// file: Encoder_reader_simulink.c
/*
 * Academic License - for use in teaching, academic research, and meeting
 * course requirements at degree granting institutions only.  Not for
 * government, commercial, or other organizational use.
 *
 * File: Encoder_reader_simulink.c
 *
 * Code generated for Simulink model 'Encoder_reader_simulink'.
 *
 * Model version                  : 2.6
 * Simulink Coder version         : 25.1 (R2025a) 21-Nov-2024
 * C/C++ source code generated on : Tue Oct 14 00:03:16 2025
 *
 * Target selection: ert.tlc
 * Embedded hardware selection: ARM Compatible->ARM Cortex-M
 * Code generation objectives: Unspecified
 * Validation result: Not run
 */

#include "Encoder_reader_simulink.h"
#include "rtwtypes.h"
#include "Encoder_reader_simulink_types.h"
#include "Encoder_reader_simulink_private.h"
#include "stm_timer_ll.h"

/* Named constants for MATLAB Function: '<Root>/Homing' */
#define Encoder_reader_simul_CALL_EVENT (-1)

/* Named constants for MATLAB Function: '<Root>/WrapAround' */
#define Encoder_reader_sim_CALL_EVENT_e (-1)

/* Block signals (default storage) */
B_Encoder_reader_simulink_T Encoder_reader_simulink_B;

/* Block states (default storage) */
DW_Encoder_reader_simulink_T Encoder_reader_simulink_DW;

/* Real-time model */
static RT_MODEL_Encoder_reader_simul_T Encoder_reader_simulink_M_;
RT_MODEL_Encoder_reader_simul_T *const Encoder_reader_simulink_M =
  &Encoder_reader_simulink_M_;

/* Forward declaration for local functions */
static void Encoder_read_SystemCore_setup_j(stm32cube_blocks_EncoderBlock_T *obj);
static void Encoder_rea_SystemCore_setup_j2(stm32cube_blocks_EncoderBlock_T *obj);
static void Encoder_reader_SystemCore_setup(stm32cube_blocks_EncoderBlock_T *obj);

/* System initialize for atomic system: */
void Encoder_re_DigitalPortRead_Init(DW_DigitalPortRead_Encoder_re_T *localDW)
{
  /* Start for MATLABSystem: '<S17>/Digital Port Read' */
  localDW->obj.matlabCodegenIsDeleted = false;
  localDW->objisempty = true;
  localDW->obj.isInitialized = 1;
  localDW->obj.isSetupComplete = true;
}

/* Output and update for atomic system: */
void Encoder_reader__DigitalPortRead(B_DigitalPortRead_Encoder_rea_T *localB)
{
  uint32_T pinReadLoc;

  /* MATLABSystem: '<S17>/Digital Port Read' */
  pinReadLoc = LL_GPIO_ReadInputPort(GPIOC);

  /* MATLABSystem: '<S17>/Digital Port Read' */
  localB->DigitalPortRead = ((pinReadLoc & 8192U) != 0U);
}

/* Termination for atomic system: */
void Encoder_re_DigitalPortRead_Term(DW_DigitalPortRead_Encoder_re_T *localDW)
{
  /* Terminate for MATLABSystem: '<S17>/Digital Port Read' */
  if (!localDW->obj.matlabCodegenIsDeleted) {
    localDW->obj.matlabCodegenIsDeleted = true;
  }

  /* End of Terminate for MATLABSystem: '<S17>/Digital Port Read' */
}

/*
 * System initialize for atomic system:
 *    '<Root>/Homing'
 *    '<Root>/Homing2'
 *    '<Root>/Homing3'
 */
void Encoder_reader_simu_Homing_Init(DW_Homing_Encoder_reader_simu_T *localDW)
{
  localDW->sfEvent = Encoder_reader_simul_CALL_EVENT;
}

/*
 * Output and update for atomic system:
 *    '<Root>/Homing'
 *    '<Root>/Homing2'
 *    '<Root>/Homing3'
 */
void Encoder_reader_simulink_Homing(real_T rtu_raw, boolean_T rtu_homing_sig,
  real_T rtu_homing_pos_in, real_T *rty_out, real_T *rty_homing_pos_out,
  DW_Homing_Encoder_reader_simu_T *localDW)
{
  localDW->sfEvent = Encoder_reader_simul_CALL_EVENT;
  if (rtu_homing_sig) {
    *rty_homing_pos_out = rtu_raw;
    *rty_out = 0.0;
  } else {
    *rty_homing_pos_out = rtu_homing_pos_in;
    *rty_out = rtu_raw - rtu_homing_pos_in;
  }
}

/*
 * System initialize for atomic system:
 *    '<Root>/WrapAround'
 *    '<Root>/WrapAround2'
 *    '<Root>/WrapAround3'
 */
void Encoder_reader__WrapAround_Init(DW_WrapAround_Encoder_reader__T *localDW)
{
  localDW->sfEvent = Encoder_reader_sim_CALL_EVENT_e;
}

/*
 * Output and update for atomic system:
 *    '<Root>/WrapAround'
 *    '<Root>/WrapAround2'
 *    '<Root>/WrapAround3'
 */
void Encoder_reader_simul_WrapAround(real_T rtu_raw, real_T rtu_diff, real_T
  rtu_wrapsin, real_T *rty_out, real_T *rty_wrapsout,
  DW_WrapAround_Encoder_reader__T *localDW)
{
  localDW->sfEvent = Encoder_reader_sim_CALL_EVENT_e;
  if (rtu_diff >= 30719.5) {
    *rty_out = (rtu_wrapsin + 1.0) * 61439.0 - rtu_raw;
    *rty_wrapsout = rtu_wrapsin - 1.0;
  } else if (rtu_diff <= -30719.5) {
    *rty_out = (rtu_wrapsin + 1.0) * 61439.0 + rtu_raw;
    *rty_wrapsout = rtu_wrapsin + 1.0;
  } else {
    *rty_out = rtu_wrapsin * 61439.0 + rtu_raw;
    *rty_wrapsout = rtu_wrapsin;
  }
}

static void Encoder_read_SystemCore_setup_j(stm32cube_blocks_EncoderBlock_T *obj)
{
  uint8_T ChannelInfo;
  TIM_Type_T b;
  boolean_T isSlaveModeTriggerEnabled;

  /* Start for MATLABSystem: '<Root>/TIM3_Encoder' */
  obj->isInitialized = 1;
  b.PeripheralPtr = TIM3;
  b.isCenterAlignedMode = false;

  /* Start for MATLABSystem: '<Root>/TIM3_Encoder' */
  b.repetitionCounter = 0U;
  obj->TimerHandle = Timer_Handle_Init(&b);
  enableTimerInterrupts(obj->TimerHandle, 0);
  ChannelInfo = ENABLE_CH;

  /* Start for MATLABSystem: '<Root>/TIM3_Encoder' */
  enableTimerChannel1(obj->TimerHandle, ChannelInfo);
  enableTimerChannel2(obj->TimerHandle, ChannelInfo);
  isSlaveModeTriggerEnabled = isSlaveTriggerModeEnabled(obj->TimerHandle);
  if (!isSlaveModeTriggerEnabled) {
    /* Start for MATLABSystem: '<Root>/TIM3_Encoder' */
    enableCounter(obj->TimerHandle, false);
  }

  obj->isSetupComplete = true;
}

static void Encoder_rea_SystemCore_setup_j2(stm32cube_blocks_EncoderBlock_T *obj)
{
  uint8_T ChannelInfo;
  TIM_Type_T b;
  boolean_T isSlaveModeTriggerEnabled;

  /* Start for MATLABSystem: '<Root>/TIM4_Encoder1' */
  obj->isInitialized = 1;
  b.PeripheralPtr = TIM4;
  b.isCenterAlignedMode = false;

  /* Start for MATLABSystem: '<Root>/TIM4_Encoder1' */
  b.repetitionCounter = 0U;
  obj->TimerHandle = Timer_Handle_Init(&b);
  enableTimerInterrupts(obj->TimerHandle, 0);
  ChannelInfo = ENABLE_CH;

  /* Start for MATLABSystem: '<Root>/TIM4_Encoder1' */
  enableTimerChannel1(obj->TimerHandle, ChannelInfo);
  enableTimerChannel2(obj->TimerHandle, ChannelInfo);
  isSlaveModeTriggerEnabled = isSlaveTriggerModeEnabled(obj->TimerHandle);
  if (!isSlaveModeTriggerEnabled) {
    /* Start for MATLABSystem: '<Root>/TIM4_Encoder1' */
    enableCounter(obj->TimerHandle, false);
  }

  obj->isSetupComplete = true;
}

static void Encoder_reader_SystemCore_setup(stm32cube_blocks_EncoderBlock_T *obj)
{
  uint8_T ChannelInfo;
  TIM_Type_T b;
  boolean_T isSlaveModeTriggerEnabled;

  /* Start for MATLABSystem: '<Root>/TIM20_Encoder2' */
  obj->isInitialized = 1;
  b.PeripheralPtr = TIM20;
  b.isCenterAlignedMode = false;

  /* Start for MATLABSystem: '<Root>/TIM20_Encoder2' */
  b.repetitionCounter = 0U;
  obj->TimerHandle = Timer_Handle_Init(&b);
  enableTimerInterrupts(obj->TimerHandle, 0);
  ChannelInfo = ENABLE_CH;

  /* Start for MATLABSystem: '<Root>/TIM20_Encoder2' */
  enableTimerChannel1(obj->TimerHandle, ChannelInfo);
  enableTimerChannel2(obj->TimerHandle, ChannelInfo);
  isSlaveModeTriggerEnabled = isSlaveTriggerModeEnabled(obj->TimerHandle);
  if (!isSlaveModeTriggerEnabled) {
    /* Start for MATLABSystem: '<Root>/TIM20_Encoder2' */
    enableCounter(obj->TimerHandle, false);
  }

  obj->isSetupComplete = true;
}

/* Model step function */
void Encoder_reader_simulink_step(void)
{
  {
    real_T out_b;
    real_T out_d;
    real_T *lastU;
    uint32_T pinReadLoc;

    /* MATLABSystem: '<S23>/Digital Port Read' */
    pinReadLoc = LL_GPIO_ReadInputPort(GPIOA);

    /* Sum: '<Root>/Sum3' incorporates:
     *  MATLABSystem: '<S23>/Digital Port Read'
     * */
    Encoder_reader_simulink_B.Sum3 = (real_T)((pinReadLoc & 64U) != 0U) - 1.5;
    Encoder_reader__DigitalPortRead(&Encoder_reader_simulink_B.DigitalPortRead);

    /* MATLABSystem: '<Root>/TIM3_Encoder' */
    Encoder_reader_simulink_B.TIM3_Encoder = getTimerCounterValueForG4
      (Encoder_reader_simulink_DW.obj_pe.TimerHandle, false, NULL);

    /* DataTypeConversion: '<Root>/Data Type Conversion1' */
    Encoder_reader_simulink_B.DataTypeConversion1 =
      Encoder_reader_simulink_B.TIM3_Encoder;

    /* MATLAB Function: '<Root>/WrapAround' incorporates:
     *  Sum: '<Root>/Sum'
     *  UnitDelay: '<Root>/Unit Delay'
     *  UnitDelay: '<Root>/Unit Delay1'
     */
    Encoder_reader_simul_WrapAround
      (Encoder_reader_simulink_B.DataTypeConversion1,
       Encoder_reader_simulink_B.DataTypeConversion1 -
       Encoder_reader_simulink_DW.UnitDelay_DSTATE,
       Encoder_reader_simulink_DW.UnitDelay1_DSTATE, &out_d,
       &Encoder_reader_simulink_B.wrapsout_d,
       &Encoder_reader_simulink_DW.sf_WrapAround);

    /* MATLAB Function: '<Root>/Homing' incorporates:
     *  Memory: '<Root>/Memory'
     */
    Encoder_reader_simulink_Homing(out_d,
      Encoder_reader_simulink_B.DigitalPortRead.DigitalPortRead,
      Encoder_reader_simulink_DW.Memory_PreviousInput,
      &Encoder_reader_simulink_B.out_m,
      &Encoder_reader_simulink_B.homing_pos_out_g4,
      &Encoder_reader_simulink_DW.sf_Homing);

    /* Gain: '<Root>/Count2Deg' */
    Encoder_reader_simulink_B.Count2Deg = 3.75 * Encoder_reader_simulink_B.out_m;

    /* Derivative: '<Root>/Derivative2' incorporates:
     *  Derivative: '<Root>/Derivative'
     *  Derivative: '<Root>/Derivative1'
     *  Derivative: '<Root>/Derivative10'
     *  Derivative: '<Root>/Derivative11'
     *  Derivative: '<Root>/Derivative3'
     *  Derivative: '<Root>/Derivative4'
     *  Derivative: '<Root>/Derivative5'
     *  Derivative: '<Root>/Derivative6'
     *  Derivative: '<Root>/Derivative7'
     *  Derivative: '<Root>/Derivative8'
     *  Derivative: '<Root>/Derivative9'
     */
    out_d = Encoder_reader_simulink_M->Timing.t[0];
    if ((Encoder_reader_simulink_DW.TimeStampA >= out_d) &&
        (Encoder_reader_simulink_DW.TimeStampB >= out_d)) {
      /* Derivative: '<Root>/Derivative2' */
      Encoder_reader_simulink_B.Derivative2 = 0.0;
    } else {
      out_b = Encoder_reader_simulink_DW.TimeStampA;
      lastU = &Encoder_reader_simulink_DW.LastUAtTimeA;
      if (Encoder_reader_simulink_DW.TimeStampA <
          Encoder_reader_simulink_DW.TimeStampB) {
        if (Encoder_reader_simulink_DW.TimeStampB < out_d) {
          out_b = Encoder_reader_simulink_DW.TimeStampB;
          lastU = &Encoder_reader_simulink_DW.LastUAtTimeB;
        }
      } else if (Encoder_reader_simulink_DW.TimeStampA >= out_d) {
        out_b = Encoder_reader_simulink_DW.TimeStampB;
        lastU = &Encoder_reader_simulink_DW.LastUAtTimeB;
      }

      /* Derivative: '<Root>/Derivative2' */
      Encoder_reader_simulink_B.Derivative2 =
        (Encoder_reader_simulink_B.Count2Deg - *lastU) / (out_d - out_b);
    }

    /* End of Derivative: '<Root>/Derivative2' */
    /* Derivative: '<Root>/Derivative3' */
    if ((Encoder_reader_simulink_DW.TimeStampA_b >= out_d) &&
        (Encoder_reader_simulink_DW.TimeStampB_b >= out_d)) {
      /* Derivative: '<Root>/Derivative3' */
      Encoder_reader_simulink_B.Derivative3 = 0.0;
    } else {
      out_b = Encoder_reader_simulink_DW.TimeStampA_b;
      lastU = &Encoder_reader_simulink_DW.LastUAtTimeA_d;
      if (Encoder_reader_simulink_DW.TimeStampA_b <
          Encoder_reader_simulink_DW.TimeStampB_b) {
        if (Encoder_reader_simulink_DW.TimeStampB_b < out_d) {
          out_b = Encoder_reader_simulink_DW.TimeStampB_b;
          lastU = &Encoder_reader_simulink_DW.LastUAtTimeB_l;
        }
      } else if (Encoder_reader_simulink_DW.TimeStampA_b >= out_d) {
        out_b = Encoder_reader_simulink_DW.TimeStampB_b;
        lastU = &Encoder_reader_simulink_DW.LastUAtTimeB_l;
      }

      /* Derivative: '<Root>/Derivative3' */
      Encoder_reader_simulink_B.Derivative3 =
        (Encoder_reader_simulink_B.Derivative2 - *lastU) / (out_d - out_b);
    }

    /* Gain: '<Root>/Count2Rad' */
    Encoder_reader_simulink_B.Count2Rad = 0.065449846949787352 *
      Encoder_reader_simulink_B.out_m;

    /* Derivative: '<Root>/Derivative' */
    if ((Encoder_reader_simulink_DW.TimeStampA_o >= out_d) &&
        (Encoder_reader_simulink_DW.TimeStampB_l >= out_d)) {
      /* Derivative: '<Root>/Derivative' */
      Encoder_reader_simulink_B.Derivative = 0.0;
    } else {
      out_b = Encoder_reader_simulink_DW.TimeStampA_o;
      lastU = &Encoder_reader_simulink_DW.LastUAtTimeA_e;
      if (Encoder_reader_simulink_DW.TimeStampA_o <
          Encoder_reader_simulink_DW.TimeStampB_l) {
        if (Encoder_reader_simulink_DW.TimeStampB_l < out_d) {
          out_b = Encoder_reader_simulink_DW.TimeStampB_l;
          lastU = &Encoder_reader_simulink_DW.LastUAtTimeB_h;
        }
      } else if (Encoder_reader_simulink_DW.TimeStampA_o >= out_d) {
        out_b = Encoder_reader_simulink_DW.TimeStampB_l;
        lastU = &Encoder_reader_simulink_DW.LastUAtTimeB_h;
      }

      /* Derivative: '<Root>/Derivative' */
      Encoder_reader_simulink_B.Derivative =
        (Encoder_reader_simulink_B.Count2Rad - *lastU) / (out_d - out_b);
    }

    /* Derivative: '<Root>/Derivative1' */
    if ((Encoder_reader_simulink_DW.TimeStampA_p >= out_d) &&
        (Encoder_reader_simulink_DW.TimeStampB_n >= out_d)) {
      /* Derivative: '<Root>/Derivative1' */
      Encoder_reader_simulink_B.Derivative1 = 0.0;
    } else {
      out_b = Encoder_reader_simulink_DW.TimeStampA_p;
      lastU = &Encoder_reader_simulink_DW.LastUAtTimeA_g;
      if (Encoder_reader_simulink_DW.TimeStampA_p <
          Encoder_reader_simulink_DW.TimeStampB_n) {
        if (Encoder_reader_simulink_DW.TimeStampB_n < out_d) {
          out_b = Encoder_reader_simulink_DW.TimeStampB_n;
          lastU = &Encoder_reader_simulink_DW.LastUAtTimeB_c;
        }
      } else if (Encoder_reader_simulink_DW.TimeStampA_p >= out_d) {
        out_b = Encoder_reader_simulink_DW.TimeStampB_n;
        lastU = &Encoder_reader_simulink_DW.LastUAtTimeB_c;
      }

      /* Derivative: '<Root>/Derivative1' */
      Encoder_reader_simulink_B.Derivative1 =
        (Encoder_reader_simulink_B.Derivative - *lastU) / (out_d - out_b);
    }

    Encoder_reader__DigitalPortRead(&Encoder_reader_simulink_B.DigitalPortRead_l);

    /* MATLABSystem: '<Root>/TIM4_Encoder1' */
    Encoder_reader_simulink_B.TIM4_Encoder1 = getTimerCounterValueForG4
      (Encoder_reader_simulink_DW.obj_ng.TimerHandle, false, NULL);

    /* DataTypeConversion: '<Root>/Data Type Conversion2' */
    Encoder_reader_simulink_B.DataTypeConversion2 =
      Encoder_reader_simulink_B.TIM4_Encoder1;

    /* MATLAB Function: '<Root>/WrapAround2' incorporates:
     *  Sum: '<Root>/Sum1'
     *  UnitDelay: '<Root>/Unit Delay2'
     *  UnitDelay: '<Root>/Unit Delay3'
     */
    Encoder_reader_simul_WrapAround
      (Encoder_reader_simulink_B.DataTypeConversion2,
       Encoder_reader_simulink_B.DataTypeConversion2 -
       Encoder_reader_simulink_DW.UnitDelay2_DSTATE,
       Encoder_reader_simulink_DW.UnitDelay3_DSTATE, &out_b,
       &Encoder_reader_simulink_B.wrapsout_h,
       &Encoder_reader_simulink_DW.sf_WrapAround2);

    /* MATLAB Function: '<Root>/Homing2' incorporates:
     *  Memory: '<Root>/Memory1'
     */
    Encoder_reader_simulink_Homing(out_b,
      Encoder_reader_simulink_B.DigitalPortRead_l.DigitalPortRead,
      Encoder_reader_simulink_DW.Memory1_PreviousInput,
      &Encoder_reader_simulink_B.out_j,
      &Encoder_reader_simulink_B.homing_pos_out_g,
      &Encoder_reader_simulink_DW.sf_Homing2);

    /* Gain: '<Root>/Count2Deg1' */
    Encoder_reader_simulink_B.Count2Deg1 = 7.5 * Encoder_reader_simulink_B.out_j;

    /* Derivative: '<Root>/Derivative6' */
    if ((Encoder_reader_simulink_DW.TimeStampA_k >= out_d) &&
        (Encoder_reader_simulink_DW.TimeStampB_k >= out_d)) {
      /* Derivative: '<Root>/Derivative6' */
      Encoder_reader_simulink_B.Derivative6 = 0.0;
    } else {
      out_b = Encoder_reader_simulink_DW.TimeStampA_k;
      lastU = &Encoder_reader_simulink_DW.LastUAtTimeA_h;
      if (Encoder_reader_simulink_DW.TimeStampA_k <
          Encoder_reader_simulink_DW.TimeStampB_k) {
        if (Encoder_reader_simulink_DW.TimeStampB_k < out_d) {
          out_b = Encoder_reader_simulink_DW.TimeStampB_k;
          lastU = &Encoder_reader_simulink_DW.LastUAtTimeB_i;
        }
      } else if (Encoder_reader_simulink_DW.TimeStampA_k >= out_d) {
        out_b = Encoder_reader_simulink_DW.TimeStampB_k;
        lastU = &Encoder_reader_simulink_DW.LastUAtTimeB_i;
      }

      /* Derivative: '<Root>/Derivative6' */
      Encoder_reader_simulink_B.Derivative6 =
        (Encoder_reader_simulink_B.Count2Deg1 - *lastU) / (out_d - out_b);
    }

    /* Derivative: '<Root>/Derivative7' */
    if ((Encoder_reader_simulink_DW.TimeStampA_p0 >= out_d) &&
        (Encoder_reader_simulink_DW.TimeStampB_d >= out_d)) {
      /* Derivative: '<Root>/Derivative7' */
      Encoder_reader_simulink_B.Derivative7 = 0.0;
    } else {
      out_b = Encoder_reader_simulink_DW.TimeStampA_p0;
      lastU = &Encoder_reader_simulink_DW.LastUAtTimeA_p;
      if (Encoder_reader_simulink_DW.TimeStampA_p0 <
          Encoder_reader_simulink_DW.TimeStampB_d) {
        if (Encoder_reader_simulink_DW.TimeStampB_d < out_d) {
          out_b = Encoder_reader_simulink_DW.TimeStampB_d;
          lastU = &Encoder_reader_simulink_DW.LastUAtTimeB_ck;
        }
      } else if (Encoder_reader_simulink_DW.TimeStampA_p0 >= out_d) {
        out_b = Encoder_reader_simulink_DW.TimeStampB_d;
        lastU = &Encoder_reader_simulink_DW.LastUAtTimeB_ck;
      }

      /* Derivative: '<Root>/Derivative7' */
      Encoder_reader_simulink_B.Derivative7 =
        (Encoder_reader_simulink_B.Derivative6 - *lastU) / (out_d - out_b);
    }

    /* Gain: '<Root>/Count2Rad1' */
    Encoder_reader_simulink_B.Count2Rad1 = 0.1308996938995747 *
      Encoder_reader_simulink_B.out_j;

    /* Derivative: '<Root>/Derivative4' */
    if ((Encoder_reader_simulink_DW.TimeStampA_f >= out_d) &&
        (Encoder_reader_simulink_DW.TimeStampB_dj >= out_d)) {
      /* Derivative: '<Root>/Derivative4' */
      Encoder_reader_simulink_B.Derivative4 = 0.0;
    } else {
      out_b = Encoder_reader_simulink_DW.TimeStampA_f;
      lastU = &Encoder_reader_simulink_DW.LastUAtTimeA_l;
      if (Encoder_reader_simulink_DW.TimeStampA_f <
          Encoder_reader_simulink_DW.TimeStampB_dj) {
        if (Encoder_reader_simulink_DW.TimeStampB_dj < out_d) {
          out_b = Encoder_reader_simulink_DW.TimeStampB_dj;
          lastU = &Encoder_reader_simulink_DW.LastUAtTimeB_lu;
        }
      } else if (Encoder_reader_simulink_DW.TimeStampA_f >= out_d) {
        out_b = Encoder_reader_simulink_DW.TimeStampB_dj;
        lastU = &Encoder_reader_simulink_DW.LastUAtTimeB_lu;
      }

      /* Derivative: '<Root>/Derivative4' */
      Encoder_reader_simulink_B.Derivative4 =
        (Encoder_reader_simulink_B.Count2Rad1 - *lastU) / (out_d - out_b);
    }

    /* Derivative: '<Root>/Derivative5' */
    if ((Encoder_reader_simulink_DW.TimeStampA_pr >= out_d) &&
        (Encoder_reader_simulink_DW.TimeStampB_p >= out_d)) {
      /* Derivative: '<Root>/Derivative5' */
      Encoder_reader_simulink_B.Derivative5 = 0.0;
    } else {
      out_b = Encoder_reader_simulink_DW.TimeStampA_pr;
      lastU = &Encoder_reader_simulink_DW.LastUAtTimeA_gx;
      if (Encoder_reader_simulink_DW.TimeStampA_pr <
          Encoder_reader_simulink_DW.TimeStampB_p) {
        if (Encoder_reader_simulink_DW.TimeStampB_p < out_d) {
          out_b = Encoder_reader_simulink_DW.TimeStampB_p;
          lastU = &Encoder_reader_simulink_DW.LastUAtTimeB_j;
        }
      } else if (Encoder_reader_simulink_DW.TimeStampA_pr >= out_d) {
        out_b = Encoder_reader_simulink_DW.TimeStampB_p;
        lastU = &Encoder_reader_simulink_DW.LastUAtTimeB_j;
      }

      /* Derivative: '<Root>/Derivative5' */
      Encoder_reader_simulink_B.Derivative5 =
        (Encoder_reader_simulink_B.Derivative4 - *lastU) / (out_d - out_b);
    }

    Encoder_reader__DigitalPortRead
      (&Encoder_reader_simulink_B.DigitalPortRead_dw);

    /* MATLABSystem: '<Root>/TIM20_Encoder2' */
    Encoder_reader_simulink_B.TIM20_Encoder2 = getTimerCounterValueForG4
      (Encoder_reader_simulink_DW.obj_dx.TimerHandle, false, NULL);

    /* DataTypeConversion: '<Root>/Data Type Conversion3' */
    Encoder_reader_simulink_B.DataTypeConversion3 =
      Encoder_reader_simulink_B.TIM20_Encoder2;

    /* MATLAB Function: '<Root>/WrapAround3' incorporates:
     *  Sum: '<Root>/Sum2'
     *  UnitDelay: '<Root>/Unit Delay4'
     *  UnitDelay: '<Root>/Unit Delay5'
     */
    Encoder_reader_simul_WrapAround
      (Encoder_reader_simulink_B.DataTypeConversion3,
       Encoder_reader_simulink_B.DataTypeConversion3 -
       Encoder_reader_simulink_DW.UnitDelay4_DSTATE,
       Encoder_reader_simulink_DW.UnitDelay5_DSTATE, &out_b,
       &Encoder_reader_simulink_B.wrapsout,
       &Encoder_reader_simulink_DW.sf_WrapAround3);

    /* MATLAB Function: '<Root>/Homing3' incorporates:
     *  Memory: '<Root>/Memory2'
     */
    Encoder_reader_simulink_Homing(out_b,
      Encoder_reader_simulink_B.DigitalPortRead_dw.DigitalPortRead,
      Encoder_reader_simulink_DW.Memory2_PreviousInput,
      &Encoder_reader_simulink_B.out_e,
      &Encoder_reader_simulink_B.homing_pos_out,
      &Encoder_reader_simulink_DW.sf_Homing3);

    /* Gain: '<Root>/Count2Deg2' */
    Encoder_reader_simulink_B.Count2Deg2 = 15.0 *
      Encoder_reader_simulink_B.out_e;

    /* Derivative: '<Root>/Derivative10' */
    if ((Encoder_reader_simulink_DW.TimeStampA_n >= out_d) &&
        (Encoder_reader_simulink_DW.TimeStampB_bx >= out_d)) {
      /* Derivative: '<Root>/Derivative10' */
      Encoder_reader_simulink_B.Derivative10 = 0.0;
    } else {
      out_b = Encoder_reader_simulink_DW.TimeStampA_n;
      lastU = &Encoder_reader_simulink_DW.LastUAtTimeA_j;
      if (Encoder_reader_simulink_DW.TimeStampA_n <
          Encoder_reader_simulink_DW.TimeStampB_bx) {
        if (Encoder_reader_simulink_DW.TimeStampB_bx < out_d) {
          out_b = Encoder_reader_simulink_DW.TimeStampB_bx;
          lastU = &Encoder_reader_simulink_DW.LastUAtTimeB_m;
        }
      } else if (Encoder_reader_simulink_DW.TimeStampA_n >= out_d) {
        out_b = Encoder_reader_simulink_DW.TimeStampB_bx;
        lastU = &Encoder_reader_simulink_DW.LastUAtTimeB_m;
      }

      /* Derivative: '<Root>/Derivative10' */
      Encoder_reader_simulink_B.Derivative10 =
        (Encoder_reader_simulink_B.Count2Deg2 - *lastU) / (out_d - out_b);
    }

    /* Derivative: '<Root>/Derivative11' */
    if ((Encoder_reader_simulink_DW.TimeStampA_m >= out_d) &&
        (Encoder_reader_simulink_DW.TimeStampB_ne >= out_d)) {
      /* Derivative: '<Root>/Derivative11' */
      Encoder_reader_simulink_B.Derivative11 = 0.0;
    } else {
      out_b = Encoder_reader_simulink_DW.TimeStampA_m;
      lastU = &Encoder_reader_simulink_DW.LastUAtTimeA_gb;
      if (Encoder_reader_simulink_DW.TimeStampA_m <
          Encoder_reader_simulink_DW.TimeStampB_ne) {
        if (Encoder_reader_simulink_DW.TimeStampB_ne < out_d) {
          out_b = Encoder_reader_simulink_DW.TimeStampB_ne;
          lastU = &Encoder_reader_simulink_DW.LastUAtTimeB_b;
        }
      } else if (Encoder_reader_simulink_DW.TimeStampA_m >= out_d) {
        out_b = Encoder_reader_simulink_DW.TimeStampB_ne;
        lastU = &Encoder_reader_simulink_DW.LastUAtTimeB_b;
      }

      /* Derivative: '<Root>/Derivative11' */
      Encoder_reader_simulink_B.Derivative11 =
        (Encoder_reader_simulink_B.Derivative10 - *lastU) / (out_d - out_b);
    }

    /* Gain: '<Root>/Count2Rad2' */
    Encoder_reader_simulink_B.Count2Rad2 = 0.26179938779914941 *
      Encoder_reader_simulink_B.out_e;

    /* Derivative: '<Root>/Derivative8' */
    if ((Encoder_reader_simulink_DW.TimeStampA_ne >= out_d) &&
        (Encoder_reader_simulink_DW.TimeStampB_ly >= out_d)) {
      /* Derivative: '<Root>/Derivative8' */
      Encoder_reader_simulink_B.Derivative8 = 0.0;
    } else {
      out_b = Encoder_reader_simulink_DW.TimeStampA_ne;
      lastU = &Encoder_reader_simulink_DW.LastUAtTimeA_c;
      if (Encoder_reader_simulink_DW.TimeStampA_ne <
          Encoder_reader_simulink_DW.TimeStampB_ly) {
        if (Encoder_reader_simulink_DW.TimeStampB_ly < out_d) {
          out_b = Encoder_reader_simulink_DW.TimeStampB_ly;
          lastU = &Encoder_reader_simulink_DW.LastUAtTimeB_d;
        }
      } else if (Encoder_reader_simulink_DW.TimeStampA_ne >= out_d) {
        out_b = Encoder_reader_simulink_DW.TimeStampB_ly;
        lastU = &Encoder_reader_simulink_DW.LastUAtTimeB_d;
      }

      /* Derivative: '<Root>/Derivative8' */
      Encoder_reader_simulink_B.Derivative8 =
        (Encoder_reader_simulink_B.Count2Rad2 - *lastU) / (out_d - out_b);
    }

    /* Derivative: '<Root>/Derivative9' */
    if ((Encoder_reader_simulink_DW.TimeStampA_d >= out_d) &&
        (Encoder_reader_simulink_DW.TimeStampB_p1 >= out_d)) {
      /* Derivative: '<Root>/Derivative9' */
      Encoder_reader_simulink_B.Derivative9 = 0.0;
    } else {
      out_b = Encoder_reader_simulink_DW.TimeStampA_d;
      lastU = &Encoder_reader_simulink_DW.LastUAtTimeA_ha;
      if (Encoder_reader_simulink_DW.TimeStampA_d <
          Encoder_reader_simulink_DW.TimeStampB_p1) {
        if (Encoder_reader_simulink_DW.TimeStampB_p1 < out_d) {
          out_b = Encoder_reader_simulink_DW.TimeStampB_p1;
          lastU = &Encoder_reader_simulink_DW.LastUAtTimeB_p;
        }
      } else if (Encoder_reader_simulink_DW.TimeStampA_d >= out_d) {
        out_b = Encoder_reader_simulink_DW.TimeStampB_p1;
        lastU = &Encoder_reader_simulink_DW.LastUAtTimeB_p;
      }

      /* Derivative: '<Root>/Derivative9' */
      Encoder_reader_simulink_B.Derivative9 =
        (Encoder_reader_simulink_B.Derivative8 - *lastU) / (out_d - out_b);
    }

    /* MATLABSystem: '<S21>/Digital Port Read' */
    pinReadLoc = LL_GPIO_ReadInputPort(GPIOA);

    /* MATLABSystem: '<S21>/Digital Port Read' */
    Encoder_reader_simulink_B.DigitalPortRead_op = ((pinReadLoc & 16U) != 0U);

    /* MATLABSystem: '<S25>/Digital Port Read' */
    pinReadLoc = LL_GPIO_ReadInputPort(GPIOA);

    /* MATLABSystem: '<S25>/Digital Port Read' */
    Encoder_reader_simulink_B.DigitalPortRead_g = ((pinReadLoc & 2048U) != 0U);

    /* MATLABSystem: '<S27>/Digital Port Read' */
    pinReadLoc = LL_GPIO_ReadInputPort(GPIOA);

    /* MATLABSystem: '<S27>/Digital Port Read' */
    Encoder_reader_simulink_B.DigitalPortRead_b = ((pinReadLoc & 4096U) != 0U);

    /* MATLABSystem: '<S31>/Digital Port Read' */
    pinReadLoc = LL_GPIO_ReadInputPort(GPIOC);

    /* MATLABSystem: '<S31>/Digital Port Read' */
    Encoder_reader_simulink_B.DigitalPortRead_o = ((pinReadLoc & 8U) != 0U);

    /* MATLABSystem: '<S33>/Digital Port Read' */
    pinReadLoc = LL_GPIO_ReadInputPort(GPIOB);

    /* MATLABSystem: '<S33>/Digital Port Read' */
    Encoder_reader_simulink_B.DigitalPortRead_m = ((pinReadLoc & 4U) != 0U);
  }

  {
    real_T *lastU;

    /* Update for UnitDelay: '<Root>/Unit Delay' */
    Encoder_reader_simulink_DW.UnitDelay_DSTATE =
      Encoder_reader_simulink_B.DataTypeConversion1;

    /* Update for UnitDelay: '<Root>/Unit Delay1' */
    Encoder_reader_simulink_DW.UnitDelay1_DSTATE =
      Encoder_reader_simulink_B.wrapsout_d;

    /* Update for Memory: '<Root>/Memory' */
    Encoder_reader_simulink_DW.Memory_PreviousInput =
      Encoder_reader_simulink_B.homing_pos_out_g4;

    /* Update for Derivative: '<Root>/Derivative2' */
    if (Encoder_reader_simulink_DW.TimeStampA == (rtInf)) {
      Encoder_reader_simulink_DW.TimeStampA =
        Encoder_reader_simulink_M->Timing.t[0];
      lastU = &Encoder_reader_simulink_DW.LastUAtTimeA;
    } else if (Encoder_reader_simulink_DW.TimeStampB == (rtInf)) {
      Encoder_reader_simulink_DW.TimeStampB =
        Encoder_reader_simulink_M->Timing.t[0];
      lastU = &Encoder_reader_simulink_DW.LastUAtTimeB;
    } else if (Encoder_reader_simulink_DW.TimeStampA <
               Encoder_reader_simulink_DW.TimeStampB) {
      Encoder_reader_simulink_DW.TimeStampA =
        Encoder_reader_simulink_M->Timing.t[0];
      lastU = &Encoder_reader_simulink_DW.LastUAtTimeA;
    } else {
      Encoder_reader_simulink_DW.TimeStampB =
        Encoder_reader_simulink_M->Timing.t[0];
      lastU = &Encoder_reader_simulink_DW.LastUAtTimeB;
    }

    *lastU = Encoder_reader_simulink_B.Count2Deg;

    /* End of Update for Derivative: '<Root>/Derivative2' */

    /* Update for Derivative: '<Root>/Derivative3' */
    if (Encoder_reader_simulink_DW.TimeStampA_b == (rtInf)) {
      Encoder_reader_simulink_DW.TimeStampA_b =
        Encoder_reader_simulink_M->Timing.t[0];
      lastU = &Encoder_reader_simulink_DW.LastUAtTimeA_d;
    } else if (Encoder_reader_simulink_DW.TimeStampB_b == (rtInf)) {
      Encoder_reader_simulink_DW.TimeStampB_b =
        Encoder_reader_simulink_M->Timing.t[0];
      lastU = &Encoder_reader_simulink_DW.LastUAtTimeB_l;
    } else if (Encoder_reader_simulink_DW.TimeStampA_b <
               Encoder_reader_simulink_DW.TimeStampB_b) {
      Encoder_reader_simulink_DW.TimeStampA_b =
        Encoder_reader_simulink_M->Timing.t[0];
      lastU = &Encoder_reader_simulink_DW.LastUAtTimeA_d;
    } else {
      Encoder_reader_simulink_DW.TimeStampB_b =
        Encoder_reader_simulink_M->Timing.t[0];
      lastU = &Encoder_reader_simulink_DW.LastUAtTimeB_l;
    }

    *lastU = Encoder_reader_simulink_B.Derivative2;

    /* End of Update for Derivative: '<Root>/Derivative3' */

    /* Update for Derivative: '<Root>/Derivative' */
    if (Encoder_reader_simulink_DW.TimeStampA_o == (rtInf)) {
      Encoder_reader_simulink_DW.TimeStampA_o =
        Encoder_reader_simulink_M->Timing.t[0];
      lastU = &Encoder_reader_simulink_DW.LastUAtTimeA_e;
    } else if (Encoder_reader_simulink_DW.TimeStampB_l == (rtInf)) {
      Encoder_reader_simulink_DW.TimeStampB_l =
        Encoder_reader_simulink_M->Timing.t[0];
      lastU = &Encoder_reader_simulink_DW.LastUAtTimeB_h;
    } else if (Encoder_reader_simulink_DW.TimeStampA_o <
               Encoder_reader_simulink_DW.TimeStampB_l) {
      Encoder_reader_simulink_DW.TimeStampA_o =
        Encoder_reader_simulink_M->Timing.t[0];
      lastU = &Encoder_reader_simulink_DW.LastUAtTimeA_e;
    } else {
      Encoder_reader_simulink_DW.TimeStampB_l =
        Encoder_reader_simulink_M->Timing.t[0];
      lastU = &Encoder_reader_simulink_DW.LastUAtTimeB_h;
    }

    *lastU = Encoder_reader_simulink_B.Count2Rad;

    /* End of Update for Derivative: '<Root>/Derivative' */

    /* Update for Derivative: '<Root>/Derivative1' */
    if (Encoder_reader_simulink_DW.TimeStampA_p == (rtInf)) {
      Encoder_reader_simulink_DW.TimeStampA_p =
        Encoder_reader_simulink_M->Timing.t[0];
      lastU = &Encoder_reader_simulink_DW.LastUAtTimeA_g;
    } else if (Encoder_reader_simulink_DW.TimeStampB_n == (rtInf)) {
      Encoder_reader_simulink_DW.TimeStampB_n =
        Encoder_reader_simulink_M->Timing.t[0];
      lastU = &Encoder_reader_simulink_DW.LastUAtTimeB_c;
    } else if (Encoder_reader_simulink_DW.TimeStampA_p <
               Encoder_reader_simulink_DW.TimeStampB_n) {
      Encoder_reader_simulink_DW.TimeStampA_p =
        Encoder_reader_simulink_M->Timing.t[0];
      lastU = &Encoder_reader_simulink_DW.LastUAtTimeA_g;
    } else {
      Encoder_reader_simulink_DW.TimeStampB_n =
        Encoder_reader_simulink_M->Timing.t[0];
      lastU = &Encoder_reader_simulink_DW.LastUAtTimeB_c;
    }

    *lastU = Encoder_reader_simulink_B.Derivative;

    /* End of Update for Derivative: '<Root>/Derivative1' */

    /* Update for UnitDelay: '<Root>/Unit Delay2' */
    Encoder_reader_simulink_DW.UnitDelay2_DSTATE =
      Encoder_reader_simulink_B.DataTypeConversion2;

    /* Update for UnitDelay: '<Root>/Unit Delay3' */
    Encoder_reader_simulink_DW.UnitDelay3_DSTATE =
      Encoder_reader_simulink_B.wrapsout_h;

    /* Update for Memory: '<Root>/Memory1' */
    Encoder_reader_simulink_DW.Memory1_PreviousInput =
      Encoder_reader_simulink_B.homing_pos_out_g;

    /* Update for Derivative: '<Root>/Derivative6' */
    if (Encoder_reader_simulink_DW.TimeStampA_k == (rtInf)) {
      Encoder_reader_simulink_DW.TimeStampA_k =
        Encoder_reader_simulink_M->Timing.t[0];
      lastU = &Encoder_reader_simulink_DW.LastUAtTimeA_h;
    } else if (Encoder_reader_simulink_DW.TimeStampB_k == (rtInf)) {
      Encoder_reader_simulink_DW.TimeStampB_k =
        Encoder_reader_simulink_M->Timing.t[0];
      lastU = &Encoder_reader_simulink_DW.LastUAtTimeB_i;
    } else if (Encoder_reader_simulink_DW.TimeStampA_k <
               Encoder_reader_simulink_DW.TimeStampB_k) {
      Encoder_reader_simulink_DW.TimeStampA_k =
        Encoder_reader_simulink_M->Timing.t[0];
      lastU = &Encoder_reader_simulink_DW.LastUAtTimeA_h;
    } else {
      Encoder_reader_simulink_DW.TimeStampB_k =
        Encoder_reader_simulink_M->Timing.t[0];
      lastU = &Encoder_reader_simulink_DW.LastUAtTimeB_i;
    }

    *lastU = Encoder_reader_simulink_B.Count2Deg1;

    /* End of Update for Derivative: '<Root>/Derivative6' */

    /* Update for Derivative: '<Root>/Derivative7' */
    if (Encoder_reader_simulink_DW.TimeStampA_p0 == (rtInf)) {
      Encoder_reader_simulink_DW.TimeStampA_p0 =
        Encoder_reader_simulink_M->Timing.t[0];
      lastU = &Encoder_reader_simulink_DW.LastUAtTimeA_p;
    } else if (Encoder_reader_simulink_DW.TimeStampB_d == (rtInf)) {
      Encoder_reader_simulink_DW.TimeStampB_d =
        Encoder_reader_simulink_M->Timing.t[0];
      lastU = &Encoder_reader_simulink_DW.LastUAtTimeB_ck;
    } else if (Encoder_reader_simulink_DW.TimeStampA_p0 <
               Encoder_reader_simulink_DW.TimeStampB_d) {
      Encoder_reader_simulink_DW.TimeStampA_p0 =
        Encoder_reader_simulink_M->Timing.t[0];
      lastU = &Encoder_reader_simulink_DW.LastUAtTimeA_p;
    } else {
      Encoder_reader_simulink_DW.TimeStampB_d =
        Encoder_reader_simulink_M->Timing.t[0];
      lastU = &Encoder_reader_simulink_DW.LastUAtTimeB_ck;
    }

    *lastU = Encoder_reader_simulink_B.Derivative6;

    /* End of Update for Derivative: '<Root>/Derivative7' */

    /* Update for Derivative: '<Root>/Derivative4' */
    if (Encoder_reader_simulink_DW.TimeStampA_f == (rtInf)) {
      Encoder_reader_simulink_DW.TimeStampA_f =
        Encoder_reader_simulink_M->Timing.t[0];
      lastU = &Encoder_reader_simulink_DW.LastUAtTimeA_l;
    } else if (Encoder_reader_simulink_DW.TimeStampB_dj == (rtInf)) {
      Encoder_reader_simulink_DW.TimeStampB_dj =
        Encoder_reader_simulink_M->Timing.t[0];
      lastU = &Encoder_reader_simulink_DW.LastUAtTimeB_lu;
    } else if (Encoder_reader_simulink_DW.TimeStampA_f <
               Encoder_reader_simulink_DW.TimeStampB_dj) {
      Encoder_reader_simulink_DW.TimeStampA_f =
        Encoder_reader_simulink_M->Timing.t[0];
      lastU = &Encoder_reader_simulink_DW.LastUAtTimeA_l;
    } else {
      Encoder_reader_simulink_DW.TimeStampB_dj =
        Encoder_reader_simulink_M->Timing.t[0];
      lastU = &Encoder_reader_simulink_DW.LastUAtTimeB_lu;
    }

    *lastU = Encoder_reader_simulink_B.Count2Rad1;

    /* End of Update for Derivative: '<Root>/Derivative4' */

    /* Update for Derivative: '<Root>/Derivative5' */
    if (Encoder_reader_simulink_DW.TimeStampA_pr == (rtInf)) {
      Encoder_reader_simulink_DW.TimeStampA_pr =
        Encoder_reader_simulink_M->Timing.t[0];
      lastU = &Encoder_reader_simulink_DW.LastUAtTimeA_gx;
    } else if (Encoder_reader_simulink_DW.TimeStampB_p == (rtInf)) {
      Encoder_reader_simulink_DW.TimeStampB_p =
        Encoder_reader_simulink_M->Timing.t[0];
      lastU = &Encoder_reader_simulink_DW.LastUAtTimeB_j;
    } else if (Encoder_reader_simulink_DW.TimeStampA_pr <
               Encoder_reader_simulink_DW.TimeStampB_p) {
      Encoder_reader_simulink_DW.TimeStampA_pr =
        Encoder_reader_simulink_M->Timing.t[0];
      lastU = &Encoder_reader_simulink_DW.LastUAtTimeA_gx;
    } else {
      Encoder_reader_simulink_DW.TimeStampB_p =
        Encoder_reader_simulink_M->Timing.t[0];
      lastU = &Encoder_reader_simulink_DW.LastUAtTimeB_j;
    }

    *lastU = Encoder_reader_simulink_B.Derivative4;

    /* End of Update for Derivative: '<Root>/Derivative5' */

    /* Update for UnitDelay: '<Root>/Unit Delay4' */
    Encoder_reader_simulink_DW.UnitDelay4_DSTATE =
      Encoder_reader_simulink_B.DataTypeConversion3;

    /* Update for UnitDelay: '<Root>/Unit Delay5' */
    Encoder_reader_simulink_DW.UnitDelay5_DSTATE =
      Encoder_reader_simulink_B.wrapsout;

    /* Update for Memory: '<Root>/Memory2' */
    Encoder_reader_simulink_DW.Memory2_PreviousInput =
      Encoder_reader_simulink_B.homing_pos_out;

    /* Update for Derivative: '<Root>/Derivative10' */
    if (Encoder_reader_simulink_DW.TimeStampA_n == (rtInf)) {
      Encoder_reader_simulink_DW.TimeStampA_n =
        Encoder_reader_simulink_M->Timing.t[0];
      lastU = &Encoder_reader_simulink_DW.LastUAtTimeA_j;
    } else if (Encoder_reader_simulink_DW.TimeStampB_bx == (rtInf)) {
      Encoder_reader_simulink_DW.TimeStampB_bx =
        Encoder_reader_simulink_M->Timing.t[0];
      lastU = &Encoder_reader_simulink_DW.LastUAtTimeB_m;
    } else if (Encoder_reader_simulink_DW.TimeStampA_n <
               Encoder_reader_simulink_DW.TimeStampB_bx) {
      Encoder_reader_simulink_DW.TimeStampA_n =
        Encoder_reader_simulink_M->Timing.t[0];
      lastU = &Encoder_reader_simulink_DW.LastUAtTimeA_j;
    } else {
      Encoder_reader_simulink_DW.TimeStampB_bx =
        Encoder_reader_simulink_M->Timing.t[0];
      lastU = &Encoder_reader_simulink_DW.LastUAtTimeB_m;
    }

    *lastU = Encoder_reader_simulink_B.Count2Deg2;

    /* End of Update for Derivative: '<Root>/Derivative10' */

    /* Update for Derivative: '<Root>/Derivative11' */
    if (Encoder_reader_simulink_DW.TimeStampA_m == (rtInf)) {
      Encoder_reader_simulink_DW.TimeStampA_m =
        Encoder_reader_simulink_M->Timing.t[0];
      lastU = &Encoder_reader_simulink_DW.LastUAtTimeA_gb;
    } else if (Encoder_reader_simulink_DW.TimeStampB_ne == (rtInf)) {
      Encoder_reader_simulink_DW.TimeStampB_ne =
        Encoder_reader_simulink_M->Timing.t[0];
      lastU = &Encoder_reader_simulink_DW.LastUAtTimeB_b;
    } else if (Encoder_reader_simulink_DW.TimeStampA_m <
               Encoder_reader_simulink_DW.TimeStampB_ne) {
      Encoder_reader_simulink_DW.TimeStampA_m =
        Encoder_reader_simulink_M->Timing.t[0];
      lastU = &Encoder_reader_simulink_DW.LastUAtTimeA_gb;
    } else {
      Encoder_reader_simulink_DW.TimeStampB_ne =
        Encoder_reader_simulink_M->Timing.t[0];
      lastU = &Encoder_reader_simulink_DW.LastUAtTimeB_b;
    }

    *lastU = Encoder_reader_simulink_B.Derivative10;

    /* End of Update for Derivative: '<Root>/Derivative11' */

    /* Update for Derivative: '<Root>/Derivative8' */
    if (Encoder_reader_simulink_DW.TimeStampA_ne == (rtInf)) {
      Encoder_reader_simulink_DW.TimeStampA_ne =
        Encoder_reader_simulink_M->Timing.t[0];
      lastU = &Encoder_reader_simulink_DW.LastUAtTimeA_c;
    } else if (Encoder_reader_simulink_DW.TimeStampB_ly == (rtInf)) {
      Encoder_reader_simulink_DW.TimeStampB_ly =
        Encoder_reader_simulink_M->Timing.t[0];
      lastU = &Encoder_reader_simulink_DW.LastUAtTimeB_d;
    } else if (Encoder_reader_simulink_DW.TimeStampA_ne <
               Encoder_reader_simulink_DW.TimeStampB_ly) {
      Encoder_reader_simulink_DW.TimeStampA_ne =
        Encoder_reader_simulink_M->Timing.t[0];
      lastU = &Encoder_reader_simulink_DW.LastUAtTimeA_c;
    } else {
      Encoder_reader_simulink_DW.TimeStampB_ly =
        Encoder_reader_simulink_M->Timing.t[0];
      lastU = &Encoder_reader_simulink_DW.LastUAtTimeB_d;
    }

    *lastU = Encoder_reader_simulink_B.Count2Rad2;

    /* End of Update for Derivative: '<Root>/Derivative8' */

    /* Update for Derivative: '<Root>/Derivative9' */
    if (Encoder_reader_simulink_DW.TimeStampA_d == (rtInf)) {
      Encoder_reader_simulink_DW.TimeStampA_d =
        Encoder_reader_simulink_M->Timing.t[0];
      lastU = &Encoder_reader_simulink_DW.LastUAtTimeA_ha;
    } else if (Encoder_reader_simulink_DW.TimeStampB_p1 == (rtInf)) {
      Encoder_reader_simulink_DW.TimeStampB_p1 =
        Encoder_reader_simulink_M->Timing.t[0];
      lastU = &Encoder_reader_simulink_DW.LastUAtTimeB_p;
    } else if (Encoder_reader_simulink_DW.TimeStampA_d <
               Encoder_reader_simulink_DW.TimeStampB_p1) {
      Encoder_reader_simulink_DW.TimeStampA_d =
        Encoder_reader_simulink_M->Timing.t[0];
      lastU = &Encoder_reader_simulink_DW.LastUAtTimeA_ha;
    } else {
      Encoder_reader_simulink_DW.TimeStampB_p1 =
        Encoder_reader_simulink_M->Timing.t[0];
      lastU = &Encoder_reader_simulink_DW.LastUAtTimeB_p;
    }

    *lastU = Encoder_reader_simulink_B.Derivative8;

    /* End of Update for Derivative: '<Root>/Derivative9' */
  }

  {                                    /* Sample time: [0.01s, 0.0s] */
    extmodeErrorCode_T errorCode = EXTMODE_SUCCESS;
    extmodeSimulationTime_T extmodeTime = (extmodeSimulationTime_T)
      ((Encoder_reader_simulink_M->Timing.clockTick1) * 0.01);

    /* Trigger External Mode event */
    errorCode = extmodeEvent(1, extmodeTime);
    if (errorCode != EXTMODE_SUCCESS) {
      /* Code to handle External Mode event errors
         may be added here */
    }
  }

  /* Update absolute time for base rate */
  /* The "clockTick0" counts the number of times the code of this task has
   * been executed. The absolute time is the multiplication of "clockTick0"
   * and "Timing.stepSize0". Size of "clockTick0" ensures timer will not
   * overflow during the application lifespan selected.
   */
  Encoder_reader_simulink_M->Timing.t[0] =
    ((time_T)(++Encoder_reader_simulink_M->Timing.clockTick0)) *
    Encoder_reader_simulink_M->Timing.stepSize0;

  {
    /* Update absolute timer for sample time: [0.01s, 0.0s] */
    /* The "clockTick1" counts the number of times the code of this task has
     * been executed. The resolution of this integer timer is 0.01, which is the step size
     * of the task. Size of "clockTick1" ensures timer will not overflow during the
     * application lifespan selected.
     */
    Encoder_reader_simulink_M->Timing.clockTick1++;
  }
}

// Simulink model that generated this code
simulink model "Encoder_reader_simulink"  (R2025a)
settings: Solver=FixedStepAuto  StartTime=0.0  StopTime=inf  FixedStep=0.01  RelTol=1e-3  EnableMultiTasking=on
libraries: stm32f4xxblockslib x18, stm32g4xxblockslib x6

== system Encoder_reader_simulink ==
  note: Rotary Encoder
  note: AMT103 Encoder
  Constant : Constant  Value=-1.5
  Constant1 : Constant  Commented=on  Value=-1.5
  Count2Deg : Gain  Gain=360/96
  Count2Deg1 : Gain  Gain=360/48
  Count2Deg2 : Gain  Gain=360/24
  Count2Deg3 : Gain  Commented=on  Gain=360/8192
  Count2Deg4 : Gain  Commented=on  Gain=360/4096
  Count2Deg5 : Gain  Commented=on  Gain=360/2048
  Count2Rad : Gain  Gain=2*pi/96
  Count2Rad1 : Gain  Gain=2*pi/48
  Count2Rad2 : Gain  Gain=2*pi/24
  Count2Rad3 : Gain  Commented=on  Gain=2*pi/8192
  Count2Rad4 : Gain  Commented=on  Gain=2*pi/4096
  Count2Rad5 : Gain  Commented=on  Gain=2*pi/2048
  Data Type Conversion1 : DataTypeConversion  OutDataTypeStr=double  SaturateOnIntegerOverflow=off  RndMeth=Floor
  Data Type Conversion2 : DataTypeConversion  OutDataTypeStr=double  SaturateOnIntegerOverflow=off  RndMeth=Floor
  Data Type Conversion3 : DataTypeConversion  OutDataTypeStr=double  SaturateOnIntegerOverflow=off  RndMeth=Floor
  Data Type Conversion4 : DataTypeConversion  Commented=on  OutDataTypeStr=double  SaturateOnIntegerOverflow=off  RndMeth=Floor
  Data Type Conversion5 : DataTypeConversion  Commented=on  OutDataTypeStr=double  SaturateOnIntegerOverflow=off  RndMeth=Floor
  Data Type Conversion6 : DataTypeConversion  Commented=on  OutDataTypeStr=double  SaturateOnIntegerOverflow=off  RndMeth=Floor
  Derivative{,1..11} (12 alike) : Derivative
  Derivative{12..23} (12 alike) : Derivative  Commented=on
  Digital Port Read : stm32f4xxblockslib/Digital Port Read  PortName=GPIOC  PinNumber=[13]  ReadOperation=on  IOAsArray=on  SampleTime=-1  EnableSimPort=off  hoistedMaskSrc=ECSoC/ECSimCodegen/Digital Port Read
  Digital Port Read1 : stm32f4xxblockslib/Digital Port Read  PortName=GPIOC  PinNumber=[13]  ReadOperation=on  IOAsArray=on  SampleTime=-1  EnableSimPort=off  hoistedMaskSrc=ECSoC/ECSimCodegen/Digital Port Read
  Digital Port Read10 : stm32f4xxblockslib/Digital Port Read  Commented=on  PortName=GPIOC  PinNumber=[13]  ReadOperation=on  IOAsArray=on  SampleTime=-1  EnableSimPort=off  hoistedMaskSrc=ECSoC/ECSimCodegen/Digital Port Read
  Digital Port Read11 : stm32f4xxblockslib/Digital Port Read  Commented=on  PortName=GPIOA  PinNumber=[4]  ReadOperation=on  IOAsArray=on  SampleTime=-1  EnableSimPort=off  hoistedMaskSrc=ECSoC/ECSimCodegen/Digital Port Read
  Digital Port Read12 : stm32f4xxblockslib/Digital Port Read  Commented=on  PortName=GPIOA  PinNumber=[6]  ReadOperation=on  IOAsArray=on  SampleTime=-1  EnableSimPort=off  hoistedMaskSrc=ECSoC/ECSimCodegen/Digital Port Read
  Digital Port Read13 : stm32f4xxblockslib/Digital Port Read  Commented=on  PortName=GPIOA  PinNumber=[11]  ReadOperation=on  IOAsArray=on  SampleTime=-1  EnableSimPort=off  hoistedMaskSrc=ECSoC/ECSimCodegen/Digital Port Read
  Digital Port Read14 : stm32f4xxblockslib/Digital Port Read  Commented=on  PortName=GPIOA  PinNumber=[12]  ReadOperation=on  IOAsArray=on  SampleTime=-1  EnableSimPort=off  hoistedMaskSrc=ECSoC/ECSimCodegen/Digital Port Read
  Digital Port Read15 : stm32f4xxblockslib/Digital Port Read  Commented=on  PortName=GPIOC  PinNumber=[13]  ReadOperation=on  IOAsArray=on  SampleTime=-1  EnableSimPort=off  hoistedMaskSrc=ECSoC/ECSimCodegen/Digital Port Read
  Digital Port Read16 : stm32f4xxblockslib/Digital Port Read  Commented=on  PortName=GPIOC  PinNumber=[3]  ReadOperation=on  IOAsArray=on  SampleTime=-1  EnableSimPort=off  hoistedMaskSrc=ECSoC/ECSimCodegen/Digital Port Read
  Digital Port Read17 : stm32f4xxblockslib/Digital Port Read  Commented=on  PortName=GPIOB  PinNumber=[2]  ReadOperation=on  IOAsArray=on  SampleTime=-1  EnableSimPort=off  hoistedMaskSrc=ECSoC/ECSimCodegen/Digital Port Read
  Digital Port Read2 : stm32f4xxblockslib/Digital Port Read  PortName=GPIOA  PinNumber=[4]  ReadOperation=on  IOAsArray=on  SampleTime=-1  EnableSimPort=off  hoistedMaskSrc=ECSoC/ECSimCodegen/Digital Port Read
  Digital Port Read3 : stm32f4xxblockslib/Digital Port Read  PortName=GPIOA  PinNumber=[6]  ReadOperation=on  IOAsArray=on  SampleTime=-1  EnableSimPort=off  hoistedMaskSrc=ECSoC/ECSimCodegen/Digital Port Read
  Digital Port Read4 : stm32f4xxblockslib/Digital Port Read  PortName=GPIOA  PinNumber=[11]  ReadOperation=on  IOAsArray=on  SampleTime=-1  EnableSimPort=off  hoistedMaskSrc=ECSoC/ECSimCodegen/Digital Port Read
  Digital Port Read5 : stm32f4xxblockslib/Digital Port Read  PortName=GPIOA  PinNumber=[12]  ReadOperation=on  IOAsArray=on  SampleTime=-1  EnableSimPort=off  hoistedMaskSrc=ECSoC/ECSimCodegen/Digital Port Read
  Digital Port Read6 : stm32f4xxblockslib/Digital Port Read  PortName=GPIOC  PinNumber=[13]  ReadOperation=on  IOAsArray=on  SampleTime=-1  EnableSimPort=off  hoistedMaskSrc=ECSoC/ECSimCodegen/Digital Port Read
  Digital Port Read7 : stm32f4xxblockslib/Digital Port Read  PortName=GPIOC  PinNumber=[3]  ReadOperation=on  IOAsArray=on  SampleTime=-1  EnableSimPort=off  hoistedMaskSrc=ECSoC/ECSimCodegen/Digital Port Read
  Digital Port Read8 : stm32f4xxblockslib/Digital Port Read  PortName=GPIOB  PinNumber=[2]  ReadOperation=on  IOAsArray=on  SampleTime=-1  EnableSimPort=off  hoistedMaskSrc=ECSoC/ECSimCodegen/Digital Port Read
  Digital Port Read9 : stm32f4xxblockslib/Digital Port Read  Commented=on  PortName=GPIOC  PinNumber=[13]  ReadOperation=on  IOAsArray=on  SampleTime=-1  EnableSimPort=off  hoistedMaskSrc=ECSoC/ECSimCodegen/Digital Port Read
  Display1 : Display
  Display2 : Display
  Display3 : Display
  Display4 : Display  Commented=on
  Display5 : Display  Commented=on
  Display6 : Display  Commented=on
  Homing : MATLAB Function  TreatAsAtomicUnit=on
  Homing1 : MATLAB Function  Commented=on  TreatAsAtomicUnit=on
  Homing2 : MATLAB Function  TreatAsAtomicUnit=on
  Homing3 : MATLAB Function  TreatAsAtomicUnit=on
  Homing4 : MATLAB Function  Commented=on  TreatAsAtomicUnit=on
  Homing5 : MATLAB Function  Commented=on  TreatAsAtomicUnit=on
  Memory : Memory
  Memory1 : Memory
  Memory2 : Memory
  Memory3 : Memory  Commented=on
  Memory4 : Memory  Commented=on
  Memory5 : Memory  Commented=on
  Sum : Sum  Inputs=|+-
  Sum1 : Sum  Inputs=|+-
  Sum2 : Sum  Inputs=|+-
  Sum3 : Sum  Inputs=|++
  Sum4 : Sum  Commented=on  Inputs=|+-
  Sum5 : Sum  Commented=on  Inputs=|+-
  Sum6 : Sum  Commented=on  Inputs=|+-
  Sum7 : Sum  Commented=on  Inputs=|++
  TIM20_Encoder1 : stm32g4xxblockslib/Encoder  Commented=on  TimerModule=TIM20  EnableResetInput=off  OutputCountAfterFirstIndex=off  OutputValidIndex=off  OutputDirection=off  OutputStatus=off  SampleTime=-1
  TIM20_Encoder2 : stm32g4xxblockslib/Encoder  TimerModule=TIM20  EnableResetInput=off  OutputCountAfterFirstIndex=off  OutputValidIndex=off  OutputDirection=off  OutputStatus=off  SampleTime=-1
  TIM3_Encoder : stm32g4xxblockslib/Encoder  TimerModule=TIM3  EnableResetInput=off  OutputCountAfterFirstIndex=off  OutputValidIndex=off  OutputDirection=off  OutputStatus=off  SampleTime=-1
  TIM3_Encoder1 : stm32g4xxblockslib/Encoder  Commented=on  TimerModule=TIM3  EnableResetInput=off  OutputCountAfterFirstIndex=off  OutputValidIndex=off  OutputDirection=off  OutputStatus=off  SampleTime=-1
  TIM4_Encoder1 : stm32g4xxblockslib/Encoder  TimerModule=TIM4  EnableResetInput=off  OutputCountAfterFirstIndex=off  OutputValidIndex=off  OutputDirection=off  OutputStatus=off  SampleTime=-1
  TIM4_Encoder2 : stm32g4xxblockslib/Encoder  Commented=on  TimerModule=TIM4  EnableResetInput=off  OutputCountAfterFirstIndex=off  OutputValidIndex=off  OutputDirection=off  OutputStatus=off  SampleTime=-1
  Unit Delay{,1..5} (6 alike) : UnitDelay  SampleTime=-1  HasFrameUpgradeWarning=on
  Unit Delay{6..11} (6 alike) : UnitDelay  Commented=on  SampleTime=-1  HasFrameUpgradeWarning=on
  WrapAround : MATLAB Function  TreatAsAtomicUnit=on
  WrapAround1 : MATLAB Function  Commented=on  TreatAsAtomicUnit=on
  WrapAround2 : MATLAB Function  TreatAsAtomicUnit=on
  WrapAround3 : MATLAB Function  TreatAsAtomicUnit=on
  WrapAround4 : MATLAB Function  Commented=on  TreatAsAtomicUnit=on
  WrapAround5 : MATLAB Function  Commented=on  TreatAsAtomicUnit=on
  wires:
  TIM3_Encoder/1 -> Data Type Conversion1/1
  Data Type Conversion1/1 -> WrapAround/1(raw), Unit Delay/1, Sum/1
  Derivative/1 -> Derivative1/1
  WrapAround/1(out) -> Homing/1(raw)
  Count2Rad/1 -> Derivative/1
  Count2Deg/1 -> Derivative2/1
  Derivative2/1 -> Derivative3/1
  Unit Delay/1 -> Sum/2
  Sum/1 -> WrapAround/2(diff)
  WrapAround/2(wrapsout) -> Unit Delay1/1
  Unit Delay1/1 -> WrapAround/3(wrapsin)
  Digital Port Read/1 -> Homing/2(homing_sig), Display1/1
  Homing/2(homing_pos_out) -> Memory/1
  Memory/1 -> Homing/3(homing_pos_in)
  Homing/1(out) -> Count2Deg/1, Count2Rad/1
  Homing2/1(out) -> Count2Deg1/1, Count2Rad1/1
  Homing2/2(homing_pos_out) -> Memory1/1
  Digital Port Read1/1 -> Homing2/2(homing_sig), Display2/1
  Memory1/1 -> Homing2/3(homing_pos_in)
  Unit Delay3/1 -> WrapAround2/3(wrapsin)
  Data Type Conversion2/1 -> Unit Delay2/1, Sum1/1, WrapAround2/1(raw)
  Derivative4/1 -> Derivative5/1
  Count2Deg1/1 -> Derivative6/1
  Sum1/1 -> WrapAround2/2(diff)
  WrapAround2/2(wrapsout) -> Unit Delay3/1
  TIM4_Encoder1/1 -> Data Type Conversion2/1
  WrapAround2/1(out) -> Homing2/1(raw)
  Derivative6/1 -> Derivative7/1
  Count2Rad1/1 -> Derivative4/1
  Unit Delay2/1 -> Sum1/2
  Homing3/1(out) -> Count2Deg2/1, Count2Rad2/1
  Unit Delay4/1 -> Sum2/2
  Derivative10/1 -> Derivative11/1
  Count2Rad2/1 -> Derivative8/1
  TIM20_Encoder2/1 -> Data Type Conversion3/1
  WrapAround3/2(wrapsout) -> Unit Delay5/1
  Count2Deg2/1 -> Derivative10/1
  Sum2/1 -> WrapAround3/2(diff)
  Data Type Conversion3/1 -> WrapAround3/1(raw), Unit Delay4/1, Sum2/1
  Derivative8/1 -> Derivative9/1
  WrapAround3/1(out) -> Homing3/1(raw)
  Memory2/1 -> Homing3/3(homing_pos_in)
  Unit Delay5/1 -> WrapAround3/3(wrapsin)
  Homing3/2(homing_pos_out) -> Memory2/1
  Digital Port Read6/1 -> Homing3/2(homing_sig), Display3/1
  Digital Port Read3/1 -> Sum3/1
  Constant/1 -> Sum3/2
  Count2Rad4/1 -> Derivative18/1
  Constant1/1 -> Sum7/2
  Derivative22/1 -> Derivative23/1
  Count2Rad3/1 -> Derivative12/1
  WrapAround5/1(out) -> Homing5/1(raw)
  Digital Port Read10/1 -> Homing4/2(homing_sig), Display5/1
  Count2Deg5/1 -> Derivative14/1
  Memory3/1 -> Homing1/3(homing_pos_in)
  Unit Delay10/1 -> Sum6/2
  TIM4_Encoder2/1 -> Data Type Conversion5/1
  Memory5/1 -> Homing5/3(homing_pos_in)
  Count2Deg4/1 -> Derivative20/1
  Unit Delay9/1 -> WrapAround4/3(wrapsin)
  Data Type Conversion6/1 -> WrapAround5/1(raw), Unit Delay10/1, Sum6/1
  Unit Delay6/1 -> Sum4/2
  Count2Deg3/1 -> Derivative16/1
  TIM3_Encoder1/1 -> Data Type Conversion4/1
  Derivative14/1 -> Derivative15/1
  Derivative20/1 -> Derivative21/1
  Derivative18/1 -> Derivative19/1
  WrapAround4/1(out) -> Homing4/1(raw)
  Digital Port Read15/1 -> Homing5/2(homing_sig), Display6/1
  Data Type Conversion4/1 -> WrapAround1/1(raw), Unit Delay6/1, Sum4/1
  Homing1/2(homing_pos_out) -> Memory3/1
  Homing5/2(homing_pos_out) -> Memory5/1
  Homing4/1(out) -> Count2Deg4/1, Count2Rad4/1
  Sum4/1 -> WrapAround1/2(diff)
  Homing5/1(out) -> Count2Deg5/1, Count2Rad5/1
  WrapAround5/2(wrapsout) -> Unit Delay11/1
  Digital Port Read9/1 -> Homing1/2(homing_sig), Display4/1
  Digital Port Read12/1 -> Sum7/1
  Derivative12/1 -> Derivative13/1
  Derivative16/1 -> Derivative17/1
  WrapAround1/2(wrapsout) -> Unit Delay7/1
  Unit Delay11/1 -> WrapAround5/3(wrapsin)
  Count2Rad5/1 -> Derivative22/1
  WrapAround4/2(wrapsout) -> Unit Delay9/1
  WrapAround1/1(out) -> Homing1/1(raw)
  Sum6/1 -> WrapAround5/2(diff)
  Homing4/2(homing_pos_out) -> Memory4/1
  TIM20_Encoder1/1 -> Data Type Conversion6/1
  Unit Delay8/1 -> Sum5/2
  Memory4/1 -> Homing4/3(homing_pos_in)
  Homing1/1(out) -> Count2Deg3/1, Count2Rad3/1
  Unit Delay7/1 -> WrapAround1/3(wrapsin)
  Data Type Conversion5/1 -> Unit Delay8/1, Sum5/1, WrapAround4/1(raw)
  Sum5/1 -> WrapAround4/2(diff)

== matlab function Encoder_reader_simulink/Homing ==
function [out,homing_pos_out]= fcn(raw, homing_sig,homing_pos_in)

if homing_sig == 1
    homing_pos_out = raw;
    out = 0;
else
    homing_pos_out = homing_pos_in;
    out = raw - homing_pos_in;
end

== matlab function Encoder_reader_simulink/WrapAround1 ==
function [out,wrapsout] = fcn(raw, diff, wrapsin)

capcity = 61439;

if diff >= capcity/2 %max
    out = -raw+(wrapsin+1)*capcity;
    wrapsout = wrapsin-1;
elseif diff <= -capcity/2 %min
    out = raw+(wrapsin+1)*capcity;
    wrapsout = wrapsin+1;
else
    out = raw+wrapsin*capcity;
    wrapsout = wrapsin;

end

== matlab function Encoder_reader_simulink/WrapAround4 ==
function [out,wrapsout] = fcn(raw, diff, wrapsin)

capcity = 61439;

if diff >= capcity/2 %max
    out = -raw+(wrapsin+1)*capcity;
    wrapsout = wrapsin-1;
elseif diff <= -capcity/2 %min
    out = raw+(wrapsin+1)*capcity;
    wrapsout = wrapsin+1;
else
    out = raw+wrapsin*capcity;
    wrapsout = wrapsin;

end

== matlab function Encoder_reader_simulink/WrapAround5 ==
function [out,wrapsout] = fcn(raw, diff, wrapsin)

capcity = 61439;

if diff >= capcity/2 %max
    out = -raw+(wrapsin+1)*capcity;
    wrapsout = wrapsin-1;
elseif diff <= -capcity/2 %min
    out = raw+(wrapsin+1)*capcity;
    wrapsout = wrapsin+1;
else
    out = raw+wrapsin*capcity;
    wrapsout = wrapsin;

end

== matlab function Encoder_reader_simulink/WrapAround ==
function [out,wrapsout] = fcn(raw, diff, wrapsin)

capcity = 61439;

if diff >= capcity/2 %max
    out = -raw+(wrapsin+1)*capcity;
    wrapsout = wrapsin-1;
elseif diff <= -capcity/2 %min
    out = raw+(wrapsin+1)*capcity;
    wrapsout = wrapsin+1;
else
    out = raw+wrapsin*capcity;
    wrapsout = wrapsin;

end

== matlab function Encoder_reader_simulink/Homing2 ==
function [out,homing_pos_out]= fcn(raw, homing_sig,homing_pos_in)

if homing_sig == 1
    homing_pos_out = raw;
    out = 0;
else
    homing_pos_out = homing_pos_in;
    out = raw - homing_pos_in;
end

== matlab function Encoder_reader_simulink/WrapAround2 ==
function [out,wrapsout] = fcn(raw, diff, wrapsin)

capcity = 61439;

if diff >= capcity/2 %max
    out = -raw+(wrapsin+1)*capcity;
    wrapsout = wrapsin-1;
elseif diff <= -capcity/2 %min
    out = raw+(wrapsin+1)*capcity;
    wrapsout = wrapsin+1;
else
    out = raw+wrapsin*capcity;
    wrapsout = wrapsin;

end

== matlab function Encoder_reader_simulink/Homing3 ==
function [out,homing_pos_out]= fcn(raw, homing_sig,homing_pos_in)

if homing_sig == 1
    homing_pos_out = raw;
    out = 0;
else
    homing_pos_out = homing_pos_in;
    out = raw - homing_pos_in;
end

== matlab function Encoder_reader_simulink/WrapAround3 ==
function [out,wrapsout] = fcn(raw, diff, wrapsin)

capcity = 61439;

if diff >= capcity/2 %max
    out = -raw+(wrapsin+1)*capcity;
    wrapsout = wrapsin-1;
elseif diff <= -capcity/2 %min
    out = raw+(wrapsin+1)*capcity;
    wrapsout = wrapsin+1;
else
    out = raw+wrapsin*capcity;
    wrapsout = wrapsin;

end

== matlab function Encoder_reader_simulink/Homing1 ==
function [out,homing_pos_out]= fcn(raw, homing_sig,homing_pos_in)

if homing_sig == 1
    homing_pos_out = raw;
    out = 0;
else
    homing_pos_out = homing_pos_in;
    out = raw - homing_pos_in;
end

== matlab function Encoder_reader_simulink/Homing4 ==
function [out,homing_pos_out]= fcn(raw, homing_sig,homing_pos_in)

if homing_sig == 1
    homing_pos_out = raw;
    out = 0;
else
    homing_pos_out = homing_pos_in;
    out = raw - homing_pos_in;
end

== matlab function Encoder_reader_simulink/Homing5 ==
function [out,homing_pos_out]= fcn(raw, homing_sig,homing_pos_in)

if homing_sig == 1
    homing_pos_out = raw;
    out = 0;
else
    homing_pos_out = homing_pos_in;
    out = raw - homing_pos_in;
end
